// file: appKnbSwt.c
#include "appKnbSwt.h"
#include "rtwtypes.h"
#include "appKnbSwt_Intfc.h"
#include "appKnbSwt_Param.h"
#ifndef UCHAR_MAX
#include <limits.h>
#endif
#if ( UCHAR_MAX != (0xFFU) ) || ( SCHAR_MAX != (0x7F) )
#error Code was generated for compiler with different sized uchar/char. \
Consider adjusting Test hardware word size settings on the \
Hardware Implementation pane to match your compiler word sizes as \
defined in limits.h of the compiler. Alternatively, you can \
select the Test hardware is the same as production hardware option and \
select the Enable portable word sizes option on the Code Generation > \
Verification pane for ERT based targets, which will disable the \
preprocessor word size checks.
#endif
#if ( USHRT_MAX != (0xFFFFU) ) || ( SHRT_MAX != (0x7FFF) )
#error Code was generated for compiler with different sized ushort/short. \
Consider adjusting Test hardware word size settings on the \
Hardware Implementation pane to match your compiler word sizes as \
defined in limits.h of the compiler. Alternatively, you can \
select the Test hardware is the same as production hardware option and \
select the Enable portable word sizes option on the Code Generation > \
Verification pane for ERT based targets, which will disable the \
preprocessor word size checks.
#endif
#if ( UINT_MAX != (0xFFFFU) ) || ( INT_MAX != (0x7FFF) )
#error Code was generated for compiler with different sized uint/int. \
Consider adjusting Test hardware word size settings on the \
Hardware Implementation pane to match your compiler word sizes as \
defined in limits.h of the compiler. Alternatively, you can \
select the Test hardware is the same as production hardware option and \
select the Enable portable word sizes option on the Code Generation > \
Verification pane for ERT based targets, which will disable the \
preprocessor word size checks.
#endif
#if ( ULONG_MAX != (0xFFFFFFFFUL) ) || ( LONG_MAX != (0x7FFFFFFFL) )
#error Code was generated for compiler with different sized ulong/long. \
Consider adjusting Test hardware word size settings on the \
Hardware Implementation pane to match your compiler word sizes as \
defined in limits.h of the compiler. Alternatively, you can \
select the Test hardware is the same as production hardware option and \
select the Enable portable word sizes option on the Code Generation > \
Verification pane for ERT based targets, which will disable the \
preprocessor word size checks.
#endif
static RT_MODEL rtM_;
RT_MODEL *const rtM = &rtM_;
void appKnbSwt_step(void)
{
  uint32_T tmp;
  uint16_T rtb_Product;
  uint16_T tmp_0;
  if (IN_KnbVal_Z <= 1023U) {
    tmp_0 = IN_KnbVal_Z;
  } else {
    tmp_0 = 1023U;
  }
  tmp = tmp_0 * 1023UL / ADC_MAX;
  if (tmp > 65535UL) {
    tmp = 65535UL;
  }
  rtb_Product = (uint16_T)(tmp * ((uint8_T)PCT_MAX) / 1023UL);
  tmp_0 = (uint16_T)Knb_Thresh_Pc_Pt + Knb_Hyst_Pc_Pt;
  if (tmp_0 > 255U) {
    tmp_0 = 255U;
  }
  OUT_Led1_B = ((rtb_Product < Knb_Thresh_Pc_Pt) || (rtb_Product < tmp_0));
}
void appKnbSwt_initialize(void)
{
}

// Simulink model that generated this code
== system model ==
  IN_KnbVal_Z : Inport
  OUT_Led1_B : Outport  <- 1: Logic#1
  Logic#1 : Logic  Operator=OR  <- 1: RelationalOperator#1, 2: RelationalOperator#2
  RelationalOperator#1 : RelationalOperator  Operator=<  <- 1: Product, 2: Knb_Thresh_Pc_Pt
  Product : Product  <- 1: Product#1, 2: PCT_MAX
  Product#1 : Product  Inputs=*/  <- 1: Saturate#1, 2: ADC_MAX
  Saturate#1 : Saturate  UpperLimit=1023  LowerLimit=0  <- 1: IN_KnbVal_Z
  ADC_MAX : Constant  Value=ADC_MAX
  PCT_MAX : Constant  Value=PCT_MAX
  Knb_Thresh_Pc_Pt : Constant  Value=Knb_Thresh_Pc_Pt
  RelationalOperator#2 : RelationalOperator  Operator=<  <- 1: Product, 2: Sum#1
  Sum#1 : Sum  <- 1: Knb_Thresh_Pc_Pt, 2: Knb_Hyst_Pc_Pt
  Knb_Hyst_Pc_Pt : Constant  Value=Knb_Hyst_Pc_Pt
